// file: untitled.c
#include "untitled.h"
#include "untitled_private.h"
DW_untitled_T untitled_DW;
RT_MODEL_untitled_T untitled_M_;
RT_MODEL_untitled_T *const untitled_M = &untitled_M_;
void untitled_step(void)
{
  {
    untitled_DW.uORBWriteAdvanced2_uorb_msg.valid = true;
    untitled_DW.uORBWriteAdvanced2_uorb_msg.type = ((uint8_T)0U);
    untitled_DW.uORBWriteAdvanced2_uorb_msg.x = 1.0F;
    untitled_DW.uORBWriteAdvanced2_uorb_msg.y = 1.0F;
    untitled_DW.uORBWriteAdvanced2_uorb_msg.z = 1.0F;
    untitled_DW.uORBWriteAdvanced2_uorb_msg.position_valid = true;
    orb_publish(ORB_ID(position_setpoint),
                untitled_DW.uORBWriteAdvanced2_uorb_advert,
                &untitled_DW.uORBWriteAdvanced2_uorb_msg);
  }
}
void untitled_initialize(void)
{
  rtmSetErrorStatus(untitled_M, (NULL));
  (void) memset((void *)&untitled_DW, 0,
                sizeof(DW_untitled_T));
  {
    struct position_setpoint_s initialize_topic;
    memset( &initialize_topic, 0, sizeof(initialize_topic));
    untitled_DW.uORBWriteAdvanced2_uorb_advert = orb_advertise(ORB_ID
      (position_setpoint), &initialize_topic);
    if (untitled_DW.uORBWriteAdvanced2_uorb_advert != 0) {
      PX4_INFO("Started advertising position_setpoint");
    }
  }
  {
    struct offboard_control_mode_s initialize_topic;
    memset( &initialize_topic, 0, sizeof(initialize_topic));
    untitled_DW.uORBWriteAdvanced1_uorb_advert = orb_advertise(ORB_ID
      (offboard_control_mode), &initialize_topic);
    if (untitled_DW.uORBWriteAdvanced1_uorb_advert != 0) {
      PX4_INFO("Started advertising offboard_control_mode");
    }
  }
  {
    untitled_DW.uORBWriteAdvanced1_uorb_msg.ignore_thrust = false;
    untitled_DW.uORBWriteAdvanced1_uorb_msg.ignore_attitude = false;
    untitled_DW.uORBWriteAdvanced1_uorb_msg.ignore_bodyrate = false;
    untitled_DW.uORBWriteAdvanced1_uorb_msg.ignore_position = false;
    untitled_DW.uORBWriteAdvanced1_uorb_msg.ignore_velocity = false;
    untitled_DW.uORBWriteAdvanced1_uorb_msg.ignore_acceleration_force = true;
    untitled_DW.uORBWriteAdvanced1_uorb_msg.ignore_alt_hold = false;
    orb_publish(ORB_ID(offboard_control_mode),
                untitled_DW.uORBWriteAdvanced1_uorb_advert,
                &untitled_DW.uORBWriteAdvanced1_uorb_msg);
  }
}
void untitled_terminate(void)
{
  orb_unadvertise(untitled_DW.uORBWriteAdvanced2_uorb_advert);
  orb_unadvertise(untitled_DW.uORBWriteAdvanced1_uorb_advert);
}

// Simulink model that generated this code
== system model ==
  uORBWriteAdvanced2 : pixhawk_slib_uORB_RW/uORB Write Advanced  <- 1: Constant#1, 2: Constant#2, 3: Constant#3, 4: Constant#4, 5: Constant#5, 6: Constant#6
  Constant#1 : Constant
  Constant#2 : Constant  Value=0
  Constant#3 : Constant
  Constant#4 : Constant
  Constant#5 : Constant
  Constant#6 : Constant
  uORBWriteAdvanced1 : pixhawk_slib_uORB_RW/uORB Write Advanced  <- 6: Constant#7
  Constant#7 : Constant
